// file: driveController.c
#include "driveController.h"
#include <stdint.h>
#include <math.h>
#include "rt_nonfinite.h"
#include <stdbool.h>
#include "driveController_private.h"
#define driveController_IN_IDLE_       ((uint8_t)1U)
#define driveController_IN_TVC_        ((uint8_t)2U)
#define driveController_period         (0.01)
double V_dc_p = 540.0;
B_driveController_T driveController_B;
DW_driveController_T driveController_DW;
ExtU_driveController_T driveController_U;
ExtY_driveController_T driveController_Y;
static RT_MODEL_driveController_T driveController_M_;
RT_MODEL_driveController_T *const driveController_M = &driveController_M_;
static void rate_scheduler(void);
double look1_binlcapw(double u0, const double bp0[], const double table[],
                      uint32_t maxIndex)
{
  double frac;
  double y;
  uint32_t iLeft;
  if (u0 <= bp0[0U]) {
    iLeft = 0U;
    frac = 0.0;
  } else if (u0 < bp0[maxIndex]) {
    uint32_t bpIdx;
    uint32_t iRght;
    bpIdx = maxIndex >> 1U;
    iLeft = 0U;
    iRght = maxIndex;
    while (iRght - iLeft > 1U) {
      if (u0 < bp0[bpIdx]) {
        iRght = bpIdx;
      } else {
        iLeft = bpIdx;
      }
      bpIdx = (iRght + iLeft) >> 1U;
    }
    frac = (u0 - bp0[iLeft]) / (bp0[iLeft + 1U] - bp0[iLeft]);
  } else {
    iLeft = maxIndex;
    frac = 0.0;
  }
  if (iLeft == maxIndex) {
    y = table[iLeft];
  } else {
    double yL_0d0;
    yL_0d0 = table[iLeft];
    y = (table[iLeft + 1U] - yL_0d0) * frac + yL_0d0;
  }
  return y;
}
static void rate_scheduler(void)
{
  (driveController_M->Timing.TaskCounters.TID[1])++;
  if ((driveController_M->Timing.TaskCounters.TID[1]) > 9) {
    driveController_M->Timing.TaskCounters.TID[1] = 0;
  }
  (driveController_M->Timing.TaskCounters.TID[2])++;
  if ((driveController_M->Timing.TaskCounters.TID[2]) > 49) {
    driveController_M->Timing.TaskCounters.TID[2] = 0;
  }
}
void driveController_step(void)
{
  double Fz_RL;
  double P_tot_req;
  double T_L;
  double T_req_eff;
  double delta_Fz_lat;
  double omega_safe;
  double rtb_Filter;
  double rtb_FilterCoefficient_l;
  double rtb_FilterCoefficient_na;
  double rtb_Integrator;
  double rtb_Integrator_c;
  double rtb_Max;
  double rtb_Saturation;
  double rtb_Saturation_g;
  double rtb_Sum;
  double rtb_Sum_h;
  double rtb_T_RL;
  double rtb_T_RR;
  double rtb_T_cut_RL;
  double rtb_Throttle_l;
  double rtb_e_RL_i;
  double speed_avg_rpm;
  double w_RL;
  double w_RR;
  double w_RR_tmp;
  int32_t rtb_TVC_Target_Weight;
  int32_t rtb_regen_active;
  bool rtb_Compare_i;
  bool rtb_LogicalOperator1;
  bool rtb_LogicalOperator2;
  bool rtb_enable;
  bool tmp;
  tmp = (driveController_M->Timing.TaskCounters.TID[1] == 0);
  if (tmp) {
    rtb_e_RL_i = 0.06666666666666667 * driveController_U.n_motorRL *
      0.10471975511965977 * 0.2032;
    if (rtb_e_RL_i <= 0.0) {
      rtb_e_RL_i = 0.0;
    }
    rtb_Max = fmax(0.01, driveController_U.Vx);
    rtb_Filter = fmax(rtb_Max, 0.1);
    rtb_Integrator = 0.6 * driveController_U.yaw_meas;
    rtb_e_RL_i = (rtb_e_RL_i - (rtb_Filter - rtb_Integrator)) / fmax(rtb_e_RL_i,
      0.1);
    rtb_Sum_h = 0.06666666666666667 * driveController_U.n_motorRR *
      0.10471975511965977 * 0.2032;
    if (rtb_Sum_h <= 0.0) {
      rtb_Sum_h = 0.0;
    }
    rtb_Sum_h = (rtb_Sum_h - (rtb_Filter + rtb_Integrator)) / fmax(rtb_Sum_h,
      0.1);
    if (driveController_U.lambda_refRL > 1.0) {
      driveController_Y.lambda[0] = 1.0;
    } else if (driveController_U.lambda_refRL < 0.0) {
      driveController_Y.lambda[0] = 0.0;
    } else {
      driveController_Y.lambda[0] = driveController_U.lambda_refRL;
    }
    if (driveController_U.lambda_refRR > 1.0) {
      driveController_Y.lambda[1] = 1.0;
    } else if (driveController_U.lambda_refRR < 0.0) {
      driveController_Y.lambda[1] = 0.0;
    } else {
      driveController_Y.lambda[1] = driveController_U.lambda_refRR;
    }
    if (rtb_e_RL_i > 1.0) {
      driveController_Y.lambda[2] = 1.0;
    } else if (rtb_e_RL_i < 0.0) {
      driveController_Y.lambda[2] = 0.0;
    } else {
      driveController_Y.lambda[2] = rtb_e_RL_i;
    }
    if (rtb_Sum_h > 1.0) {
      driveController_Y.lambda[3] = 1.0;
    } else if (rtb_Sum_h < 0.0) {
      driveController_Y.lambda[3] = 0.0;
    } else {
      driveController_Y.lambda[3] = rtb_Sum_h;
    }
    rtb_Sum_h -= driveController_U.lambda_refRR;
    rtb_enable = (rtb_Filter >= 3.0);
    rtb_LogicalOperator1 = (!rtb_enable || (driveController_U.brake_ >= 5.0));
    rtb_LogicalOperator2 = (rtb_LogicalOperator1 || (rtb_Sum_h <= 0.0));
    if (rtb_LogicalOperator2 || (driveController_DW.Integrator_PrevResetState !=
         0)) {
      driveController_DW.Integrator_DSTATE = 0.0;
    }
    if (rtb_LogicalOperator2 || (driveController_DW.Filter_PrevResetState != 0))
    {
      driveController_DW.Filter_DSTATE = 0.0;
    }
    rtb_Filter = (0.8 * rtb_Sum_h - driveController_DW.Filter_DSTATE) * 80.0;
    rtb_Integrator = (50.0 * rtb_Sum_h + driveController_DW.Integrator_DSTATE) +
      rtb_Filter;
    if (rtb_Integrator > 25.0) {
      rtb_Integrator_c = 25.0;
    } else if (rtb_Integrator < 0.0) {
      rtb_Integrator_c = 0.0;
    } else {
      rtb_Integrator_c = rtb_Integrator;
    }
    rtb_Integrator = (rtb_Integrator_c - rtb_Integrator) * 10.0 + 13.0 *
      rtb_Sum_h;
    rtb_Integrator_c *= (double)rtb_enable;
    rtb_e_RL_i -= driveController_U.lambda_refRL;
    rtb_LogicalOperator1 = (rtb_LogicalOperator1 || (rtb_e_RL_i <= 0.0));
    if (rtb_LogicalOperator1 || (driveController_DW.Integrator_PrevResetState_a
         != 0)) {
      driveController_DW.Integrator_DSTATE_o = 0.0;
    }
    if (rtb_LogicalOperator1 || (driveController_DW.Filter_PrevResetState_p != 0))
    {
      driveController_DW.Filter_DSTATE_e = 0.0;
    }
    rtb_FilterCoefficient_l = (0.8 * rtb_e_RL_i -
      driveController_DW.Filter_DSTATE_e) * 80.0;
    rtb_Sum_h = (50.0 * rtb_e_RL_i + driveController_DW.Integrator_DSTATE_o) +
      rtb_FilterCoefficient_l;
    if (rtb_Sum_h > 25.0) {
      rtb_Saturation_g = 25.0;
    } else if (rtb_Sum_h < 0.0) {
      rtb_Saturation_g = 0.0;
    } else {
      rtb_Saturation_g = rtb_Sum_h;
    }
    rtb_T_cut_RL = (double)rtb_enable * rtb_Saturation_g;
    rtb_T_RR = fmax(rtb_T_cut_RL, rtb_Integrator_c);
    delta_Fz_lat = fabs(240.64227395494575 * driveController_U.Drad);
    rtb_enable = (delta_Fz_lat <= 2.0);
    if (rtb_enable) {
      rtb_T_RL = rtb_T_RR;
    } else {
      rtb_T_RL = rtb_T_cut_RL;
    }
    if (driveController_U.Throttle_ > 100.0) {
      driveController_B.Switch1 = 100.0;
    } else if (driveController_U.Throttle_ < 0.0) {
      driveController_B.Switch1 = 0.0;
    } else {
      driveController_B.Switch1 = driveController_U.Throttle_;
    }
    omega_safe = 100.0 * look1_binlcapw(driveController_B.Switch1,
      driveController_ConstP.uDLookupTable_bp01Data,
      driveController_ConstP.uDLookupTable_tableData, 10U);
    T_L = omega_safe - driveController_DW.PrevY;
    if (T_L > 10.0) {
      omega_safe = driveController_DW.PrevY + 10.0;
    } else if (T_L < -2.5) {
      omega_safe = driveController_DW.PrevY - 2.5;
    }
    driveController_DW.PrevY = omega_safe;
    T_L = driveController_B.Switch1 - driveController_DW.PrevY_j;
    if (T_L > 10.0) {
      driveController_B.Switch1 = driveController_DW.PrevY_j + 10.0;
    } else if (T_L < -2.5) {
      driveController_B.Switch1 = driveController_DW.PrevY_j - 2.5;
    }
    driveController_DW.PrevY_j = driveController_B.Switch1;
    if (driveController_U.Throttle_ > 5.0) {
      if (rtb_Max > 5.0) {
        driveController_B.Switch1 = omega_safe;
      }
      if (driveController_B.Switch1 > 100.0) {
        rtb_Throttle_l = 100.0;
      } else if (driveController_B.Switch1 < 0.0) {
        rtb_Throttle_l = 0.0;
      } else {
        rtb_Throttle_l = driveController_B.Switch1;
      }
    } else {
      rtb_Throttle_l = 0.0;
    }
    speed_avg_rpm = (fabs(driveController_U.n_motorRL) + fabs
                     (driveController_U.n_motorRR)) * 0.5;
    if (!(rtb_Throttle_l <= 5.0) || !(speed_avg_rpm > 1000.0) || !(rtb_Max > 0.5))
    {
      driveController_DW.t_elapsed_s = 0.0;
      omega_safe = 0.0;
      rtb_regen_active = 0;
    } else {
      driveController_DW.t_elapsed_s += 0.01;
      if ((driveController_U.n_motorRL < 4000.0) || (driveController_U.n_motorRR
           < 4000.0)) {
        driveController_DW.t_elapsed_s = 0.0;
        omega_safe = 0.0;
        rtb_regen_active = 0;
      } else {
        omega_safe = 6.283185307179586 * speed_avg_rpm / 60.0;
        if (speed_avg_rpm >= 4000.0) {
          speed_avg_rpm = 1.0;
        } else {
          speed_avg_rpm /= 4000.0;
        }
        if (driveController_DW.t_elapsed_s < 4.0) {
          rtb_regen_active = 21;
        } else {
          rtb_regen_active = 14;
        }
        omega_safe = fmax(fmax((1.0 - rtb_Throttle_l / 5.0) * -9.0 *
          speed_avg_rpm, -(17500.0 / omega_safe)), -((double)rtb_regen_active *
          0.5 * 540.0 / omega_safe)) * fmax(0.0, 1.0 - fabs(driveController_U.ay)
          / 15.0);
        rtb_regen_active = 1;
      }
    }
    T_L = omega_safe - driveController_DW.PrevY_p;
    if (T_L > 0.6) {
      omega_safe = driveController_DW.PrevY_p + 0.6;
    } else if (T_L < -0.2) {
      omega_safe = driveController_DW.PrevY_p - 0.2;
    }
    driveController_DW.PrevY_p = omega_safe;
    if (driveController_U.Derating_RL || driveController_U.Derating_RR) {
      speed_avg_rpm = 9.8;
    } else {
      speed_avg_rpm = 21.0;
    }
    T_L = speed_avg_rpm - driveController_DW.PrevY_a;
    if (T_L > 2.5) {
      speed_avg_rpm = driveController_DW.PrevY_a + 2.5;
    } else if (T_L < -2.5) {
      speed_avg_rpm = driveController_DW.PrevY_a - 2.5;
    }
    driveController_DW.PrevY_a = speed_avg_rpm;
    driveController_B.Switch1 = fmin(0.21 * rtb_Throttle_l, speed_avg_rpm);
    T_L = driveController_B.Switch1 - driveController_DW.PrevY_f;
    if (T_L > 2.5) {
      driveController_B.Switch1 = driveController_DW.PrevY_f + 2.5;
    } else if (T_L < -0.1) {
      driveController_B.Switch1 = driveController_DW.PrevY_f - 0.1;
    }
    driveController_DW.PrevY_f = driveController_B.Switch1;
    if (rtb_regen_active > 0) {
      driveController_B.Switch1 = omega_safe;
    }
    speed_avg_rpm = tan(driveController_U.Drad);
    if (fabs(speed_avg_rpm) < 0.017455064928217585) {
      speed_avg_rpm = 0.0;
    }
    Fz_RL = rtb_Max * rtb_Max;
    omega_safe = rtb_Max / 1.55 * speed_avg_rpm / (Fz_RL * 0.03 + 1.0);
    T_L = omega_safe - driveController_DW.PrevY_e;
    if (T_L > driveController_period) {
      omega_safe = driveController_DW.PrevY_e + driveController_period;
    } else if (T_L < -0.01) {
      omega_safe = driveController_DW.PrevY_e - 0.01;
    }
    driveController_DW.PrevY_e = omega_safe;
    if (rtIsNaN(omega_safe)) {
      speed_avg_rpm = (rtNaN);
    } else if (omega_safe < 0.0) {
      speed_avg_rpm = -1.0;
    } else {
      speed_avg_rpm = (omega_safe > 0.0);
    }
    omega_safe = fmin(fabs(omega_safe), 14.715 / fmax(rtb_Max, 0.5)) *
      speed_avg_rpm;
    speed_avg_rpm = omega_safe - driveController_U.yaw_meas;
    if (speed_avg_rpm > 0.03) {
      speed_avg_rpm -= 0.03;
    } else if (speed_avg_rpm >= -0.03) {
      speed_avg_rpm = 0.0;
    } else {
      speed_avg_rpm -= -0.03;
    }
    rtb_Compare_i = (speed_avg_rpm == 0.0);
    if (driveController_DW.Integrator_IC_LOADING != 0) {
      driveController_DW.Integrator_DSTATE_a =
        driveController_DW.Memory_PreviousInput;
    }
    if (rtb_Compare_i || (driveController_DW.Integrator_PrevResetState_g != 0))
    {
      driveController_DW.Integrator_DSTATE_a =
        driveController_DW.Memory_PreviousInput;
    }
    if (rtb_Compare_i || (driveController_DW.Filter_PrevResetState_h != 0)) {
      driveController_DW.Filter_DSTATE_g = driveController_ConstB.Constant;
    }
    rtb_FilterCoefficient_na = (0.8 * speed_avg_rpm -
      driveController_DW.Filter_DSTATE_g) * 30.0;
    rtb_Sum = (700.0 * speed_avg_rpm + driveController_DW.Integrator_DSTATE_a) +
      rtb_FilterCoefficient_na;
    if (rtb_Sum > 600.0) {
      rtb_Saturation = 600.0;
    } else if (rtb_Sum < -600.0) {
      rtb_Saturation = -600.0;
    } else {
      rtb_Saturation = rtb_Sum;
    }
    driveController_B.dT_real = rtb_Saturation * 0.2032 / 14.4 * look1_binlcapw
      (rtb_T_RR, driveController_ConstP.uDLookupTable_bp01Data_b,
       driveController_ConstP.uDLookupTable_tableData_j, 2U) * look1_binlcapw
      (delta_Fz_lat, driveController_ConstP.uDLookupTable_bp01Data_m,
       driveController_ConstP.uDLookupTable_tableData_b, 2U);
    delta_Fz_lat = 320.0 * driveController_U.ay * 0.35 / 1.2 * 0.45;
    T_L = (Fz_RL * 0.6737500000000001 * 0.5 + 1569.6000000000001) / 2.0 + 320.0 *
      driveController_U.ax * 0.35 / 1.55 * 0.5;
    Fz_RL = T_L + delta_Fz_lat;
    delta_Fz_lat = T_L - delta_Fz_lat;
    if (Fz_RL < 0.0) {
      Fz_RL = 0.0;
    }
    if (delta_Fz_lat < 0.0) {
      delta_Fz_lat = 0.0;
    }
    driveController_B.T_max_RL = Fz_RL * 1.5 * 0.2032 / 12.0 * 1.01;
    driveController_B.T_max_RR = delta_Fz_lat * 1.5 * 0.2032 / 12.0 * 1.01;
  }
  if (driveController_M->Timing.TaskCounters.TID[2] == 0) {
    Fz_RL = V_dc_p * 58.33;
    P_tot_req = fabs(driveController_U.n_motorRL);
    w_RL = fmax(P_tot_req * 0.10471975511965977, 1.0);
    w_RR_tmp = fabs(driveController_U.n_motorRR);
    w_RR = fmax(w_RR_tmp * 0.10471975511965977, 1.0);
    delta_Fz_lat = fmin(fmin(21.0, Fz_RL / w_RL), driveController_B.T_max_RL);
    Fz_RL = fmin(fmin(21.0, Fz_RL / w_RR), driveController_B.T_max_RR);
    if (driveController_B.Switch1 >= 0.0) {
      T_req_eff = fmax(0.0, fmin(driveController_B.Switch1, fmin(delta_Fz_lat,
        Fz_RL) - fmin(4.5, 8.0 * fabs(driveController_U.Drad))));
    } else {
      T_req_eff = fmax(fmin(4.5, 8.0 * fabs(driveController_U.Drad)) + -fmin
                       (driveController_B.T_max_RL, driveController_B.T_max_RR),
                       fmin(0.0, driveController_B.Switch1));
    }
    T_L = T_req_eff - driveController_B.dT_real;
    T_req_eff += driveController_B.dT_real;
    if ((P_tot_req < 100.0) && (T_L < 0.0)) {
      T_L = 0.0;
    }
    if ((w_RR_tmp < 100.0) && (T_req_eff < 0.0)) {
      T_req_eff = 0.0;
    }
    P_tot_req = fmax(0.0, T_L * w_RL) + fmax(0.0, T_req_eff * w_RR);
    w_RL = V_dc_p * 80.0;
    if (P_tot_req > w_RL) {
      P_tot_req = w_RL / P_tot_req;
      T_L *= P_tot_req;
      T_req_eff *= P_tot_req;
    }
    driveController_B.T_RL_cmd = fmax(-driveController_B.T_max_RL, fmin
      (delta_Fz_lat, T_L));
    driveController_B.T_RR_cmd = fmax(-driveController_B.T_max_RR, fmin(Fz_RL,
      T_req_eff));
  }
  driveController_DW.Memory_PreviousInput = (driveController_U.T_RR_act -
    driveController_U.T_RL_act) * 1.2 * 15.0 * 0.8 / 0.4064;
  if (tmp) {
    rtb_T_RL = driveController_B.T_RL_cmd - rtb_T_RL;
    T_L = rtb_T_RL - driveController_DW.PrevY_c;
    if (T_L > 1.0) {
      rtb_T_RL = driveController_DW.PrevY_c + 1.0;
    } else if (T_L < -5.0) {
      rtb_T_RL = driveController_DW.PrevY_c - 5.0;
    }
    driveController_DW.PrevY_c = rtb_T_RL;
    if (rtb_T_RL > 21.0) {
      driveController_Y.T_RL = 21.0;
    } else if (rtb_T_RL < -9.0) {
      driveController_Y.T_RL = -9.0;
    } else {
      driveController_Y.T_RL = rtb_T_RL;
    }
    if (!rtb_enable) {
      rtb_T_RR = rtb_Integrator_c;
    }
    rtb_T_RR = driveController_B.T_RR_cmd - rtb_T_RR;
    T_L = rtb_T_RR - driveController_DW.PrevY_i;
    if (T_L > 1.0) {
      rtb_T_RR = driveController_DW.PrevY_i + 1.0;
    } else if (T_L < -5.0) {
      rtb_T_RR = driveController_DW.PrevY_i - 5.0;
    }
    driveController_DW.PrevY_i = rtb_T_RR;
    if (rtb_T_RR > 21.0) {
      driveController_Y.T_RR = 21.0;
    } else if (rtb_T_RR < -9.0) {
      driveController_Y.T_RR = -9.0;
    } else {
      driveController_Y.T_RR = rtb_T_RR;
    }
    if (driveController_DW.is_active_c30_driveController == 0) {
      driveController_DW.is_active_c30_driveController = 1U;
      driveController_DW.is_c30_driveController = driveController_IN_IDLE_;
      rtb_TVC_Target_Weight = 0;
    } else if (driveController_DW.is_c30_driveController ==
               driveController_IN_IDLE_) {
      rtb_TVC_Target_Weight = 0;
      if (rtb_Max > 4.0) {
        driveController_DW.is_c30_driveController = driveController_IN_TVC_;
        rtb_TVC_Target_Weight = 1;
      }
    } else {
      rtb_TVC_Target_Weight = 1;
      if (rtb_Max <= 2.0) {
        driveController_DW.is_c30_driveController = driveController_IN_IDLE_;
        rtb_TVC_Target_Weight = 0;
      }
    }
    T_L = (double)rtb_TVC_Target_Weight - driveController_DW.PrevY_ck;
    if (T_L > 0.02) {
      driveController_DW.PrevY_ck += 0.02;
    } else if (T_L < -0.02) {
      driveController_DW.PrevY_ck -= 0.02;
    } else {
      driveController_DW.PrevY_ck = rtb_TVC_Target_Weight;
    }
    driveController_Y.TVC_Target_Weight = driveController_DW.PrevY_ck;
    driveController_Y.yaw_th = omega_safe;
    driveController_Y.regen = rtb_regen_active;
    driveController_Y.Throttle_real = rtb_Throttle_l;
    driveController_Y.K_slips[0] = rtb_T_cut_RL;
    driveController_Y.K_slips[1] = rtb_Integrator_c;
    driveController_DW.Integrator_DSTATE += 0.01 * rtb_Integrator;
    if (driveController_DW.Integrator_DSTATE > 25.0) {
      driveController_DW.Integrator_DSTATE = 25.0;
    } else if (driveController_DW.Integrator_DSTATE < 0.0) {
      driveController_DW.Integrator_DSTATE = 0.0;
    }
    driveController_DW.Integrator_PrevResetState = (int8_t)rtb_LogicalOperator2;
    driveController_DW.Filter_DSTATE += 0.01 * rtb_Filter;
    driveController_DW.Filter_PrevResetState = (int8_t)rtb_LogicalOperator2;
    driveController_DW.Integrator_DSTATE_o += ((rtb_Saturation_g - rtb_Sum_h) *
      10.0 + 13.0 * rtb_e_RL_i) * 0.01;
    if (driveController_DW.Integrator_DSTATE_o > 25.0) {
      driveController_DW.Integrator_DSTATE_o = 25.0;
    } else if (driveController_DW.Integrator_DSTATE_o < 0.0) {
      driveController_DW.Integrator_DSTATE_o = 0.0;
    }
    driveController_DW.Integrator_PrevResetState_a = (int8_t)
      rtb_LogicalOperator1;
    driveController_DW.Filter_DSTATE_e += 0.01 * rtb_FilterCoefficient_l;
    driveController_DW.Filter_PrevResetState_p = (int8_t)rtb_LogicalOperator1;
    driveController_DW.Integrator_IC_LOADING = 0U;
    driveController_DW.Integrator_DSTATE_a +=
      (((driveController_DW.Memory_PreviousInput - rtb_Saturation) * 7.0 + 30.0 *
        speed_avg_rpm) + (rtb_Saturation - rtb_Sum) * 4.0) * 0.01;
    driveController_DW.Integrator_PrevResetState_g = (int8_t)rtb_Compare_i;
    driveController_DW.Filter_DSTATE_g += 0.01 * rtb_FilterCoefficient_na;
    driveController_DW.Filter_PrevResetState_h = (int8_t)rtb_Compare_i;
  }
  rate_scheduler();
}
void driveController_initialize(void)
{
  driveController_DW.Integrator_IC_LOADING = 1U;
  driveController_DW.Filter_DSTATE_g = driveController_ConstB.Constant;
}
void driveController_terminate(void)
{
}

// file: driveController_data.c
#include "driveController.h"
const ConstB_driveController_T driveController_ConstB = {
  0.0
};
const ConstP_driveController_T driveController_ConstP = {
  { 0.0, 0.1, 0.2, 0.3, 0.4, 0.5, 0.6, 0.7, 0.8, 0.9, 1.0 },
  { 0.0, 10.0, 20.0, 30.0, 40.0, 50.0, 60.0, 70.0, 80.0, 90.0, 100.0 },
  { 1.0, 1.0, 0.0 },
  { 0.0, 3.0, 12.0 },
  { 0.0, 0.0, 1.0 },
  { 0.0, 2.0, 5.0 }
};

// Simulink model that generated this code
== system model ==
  Throttle_ : Inport
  Vx : Inport
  ax : Inport
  ay : Inport
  Inport#1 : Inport
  Inport#2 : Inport
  brake_ : Inport
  T_RL_act : Inport
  T_RR_act : Inport
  Derating_RL : Inport
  Derating_RR : Inport
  n_motorRL : Inport
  n_motorRR : Inport
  lambda_refRL : Inport
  lambda_refRR : Inport
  T_RL : Outport  <- 1: Saturate#1
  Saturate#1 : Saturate  UpperLimit=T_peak  LowerLimit=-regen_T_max  <- 1: RateLimiter#1
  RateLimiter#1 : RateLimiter  RisingSlewLimit=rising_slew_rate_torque  FallingSlewLimit=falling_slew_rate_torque  <- 1: Sum#1
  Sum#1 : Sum  Inputs=+-  <- 1: MATLABFunction#1, 2: Switch#1
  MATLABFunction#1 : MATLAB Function  <- 1: Switch1, 2: Product#1, 3: n_motorRL, 4: n_motorRR, 5: Inport#2, 6: MATLABFunction#2, 7: MATLABFunction#2/2
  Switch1 : Switch  Criteria=u2 > Threshold  <- 1: RateLimiter#2, 2: MATLABFunction#3/2, 3: RateLimiter#3
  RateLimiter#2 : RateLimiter  RisingSlewLimit=60  FallingSlewLimit=-20  <- 1: MATLABFunction#3
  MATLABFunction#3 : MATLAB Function  <- 1: Switch#2, 2: n_motorRL, 3: n_motorRR, 4: Max, 5: ay
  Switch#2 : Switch  Criteria=u2 > Threshold  Threshold=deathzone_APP  <- 1: Saturation, 2: Throttle_, 3: Constant
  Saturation : Saturate  UpperLimit=100  LowerLimit=0  <- 1: Switch#3
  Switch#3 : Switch  Criteria=u2 > Threshold  Threshold=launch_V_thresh  <- 1: RateLimiter#4, 2: Max, 3: RateLimiter#5
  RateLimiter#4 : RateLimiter  RisingSlewLimit=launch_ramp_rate  FallingSlewLimit=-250  <- 1: Gain#1
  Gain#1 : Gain  Gain=100  <- 1: Lookup_nD#1
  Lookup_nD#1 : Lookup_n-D  BreakpointsForDimension1=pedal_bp  Table=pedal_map  <- 1: Saturate#2
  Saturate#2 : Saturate  UpperLimit=100  LowerLimit=0  <- 1: Throttle_
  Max : MinMax  Function=max  Inputs=2  <- 1: Constant#1, 2: Vx
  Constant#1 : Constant  Value=0.01
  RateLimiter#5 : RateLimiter  RisingSlewLimit=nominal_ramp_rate  FallingSlewLimit=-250  <- 1: Saturate#2
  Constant : Constant  Value=0
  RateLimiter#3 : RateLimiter  RisingSlewLimit=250  FallingSlewLimit=-10  <- 1: MinMax#1
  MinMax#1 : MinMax  Inputs=2  <- 1: Gain#2, 2: RateLimiter#6
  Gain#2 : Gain  Gain=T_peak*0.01  <- 1: Switch#2
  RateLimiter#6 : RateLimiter  RisingSlewLimit=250  FallingSlewLimit=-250  <- 1: Switch#4
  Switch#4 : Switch  Criteria=u2 > Threshold  Threshold=0.5  <- 1: Constant#2, 2: Logic#1, 3: Constant#3
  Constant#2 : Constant  Value=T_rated
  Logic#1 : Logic  Operator=OR  <- 1: Derating_RL, 2: Derating_RR
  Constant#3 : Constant  Value=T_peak
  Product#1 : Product  Inputs=3  <- 1: MATLABFunction#4, 2: Lookup_nD#2, 3: Lookup_nD#3
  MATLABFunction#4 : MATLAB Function  <- 1: PIDController#1
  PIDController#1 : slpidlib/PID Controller  Controller=PID  Form=Parallel  TimeDomain=Discrete-time  IntegratorMethod=Forward Euler  P=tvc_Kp  I=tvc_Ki  D=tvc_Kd  N=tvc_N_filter  InitialConditionForIntegrator=0  ExternalReset=level  LimitOutput=on  UpperSaturationLimit=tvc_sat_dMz  LowerSaturationLimit=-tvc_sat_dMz  <- 1: DeadZone#1, 2: CompareToConstant#1, 3: Memory, 4: Constant#4, 5: MATLABFunction#5
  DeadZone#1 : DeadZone  LowerValue=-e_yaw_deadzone  UpperValue=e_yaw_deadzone  <- 1: Sum
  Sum : Sum  Inputs=+-  <- 1: MATLABFunction#6, 2: Inport#1
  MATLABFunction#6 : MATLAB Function  <- 1: RateLimiter#7, 2: Max
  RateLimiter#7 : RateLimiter  <- 1: MATLABFunction#7
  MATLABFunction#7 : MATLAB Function  <- 1: Max, 2: MATLABFunction#8
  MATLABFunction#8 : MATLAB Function  <- 1: Trigonometry#1
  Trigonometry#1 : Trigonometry  Operator=tan  <- 1: Inport#2
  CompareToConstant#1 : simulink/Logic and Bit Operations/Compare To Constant  relop===  const=0  <- 1: DeadZone#1
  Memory : Memory  <- 1: MATLABFunction#5
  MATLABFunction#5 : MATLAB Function  <- 1: Sum#2
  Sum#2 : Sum  Inputs=-+  <- 1: T_RL_act, 2: T_RR_act
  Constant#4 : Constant  Value=0
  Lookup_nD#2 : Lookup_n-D  BreakpointsForDimension1=[0,3,12]  Table=[1,1,0]  <- 1: MinMax#2
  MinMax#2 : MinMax  Function=max  Inputs=2  <- 1: MATLABFunction#9, 2: MATLABFunction#10
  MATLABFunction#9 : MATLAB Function  <- 1: RelationalOperator#1, 2: Saturate#3
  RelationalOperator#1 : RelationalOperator  <- 1: MinMax#3, 2: Constant#5
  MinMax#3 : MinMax  Function=max  Inputs=2  <- 1: Max, 2: Constant#6
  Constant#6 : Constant  Value=0.1
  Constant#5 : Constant  Value=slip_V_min
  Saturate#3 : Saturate  UpperLimit=inf  LowerLimit=-2  <- 1: PIDController#2
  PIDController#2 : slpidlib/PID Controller  Controller=PID  Form=Parallel  TimeDomain=Discrete-time  IntegratorMethod=Forward Euler  P=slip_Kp  I=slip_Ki  D=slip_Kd  N=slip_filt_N  InitialConditionForIntegrator=0  ExternalReset=level  LimitOutput=on  UpperSaturationLimit=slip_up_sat  LowerSaturationLimit=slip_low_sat  <- 1: Sum#3, 2: LogicalOperator1
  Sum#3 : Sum  Inputs=-+  <- 1: lambda_refRL, 2: Product#2
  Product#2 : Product  Inputs=*/  <- 1: Sum#4, 2: MinMax#4
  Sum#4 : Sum  Inputs=+-  <- 1: Saturate#4, 2: Sum#5
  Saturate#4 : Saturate  UpperLimit=inf  LowerLimit=0  <- 1: Gain#3
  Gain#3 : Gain  Gain=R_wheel  <- 1: Gain#4
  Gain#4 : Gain  Gain=2*pi/60  <- 1: Gain#5
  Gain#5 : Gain  Gain=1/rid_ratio  <- 1: n_motorRL
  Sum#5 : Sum  Inputs=+-  <- 1: MinMax#3, 2: Gain#6
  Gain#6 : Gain  Gain=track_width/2  <- 1: Inport#1
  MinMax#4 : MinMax  Function=max  Inputs=2  <- 1: Saturate#4, 2: Constant#7
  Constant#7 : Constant  Value=0.1
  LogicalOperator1 : Logic  Operator=OR  Inputs=3  <- 1: Logic#2, 2: CompareToConstant#2, 3: CompareToConstant#3
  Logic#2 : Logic  Operator=NOT  <- 1: RelationalOperator#1
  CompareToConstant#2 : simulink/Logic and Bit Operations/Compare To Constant  relop=>=  const=5  <- 1: brake_
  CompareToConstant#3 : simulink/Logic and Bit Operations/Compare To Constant  relop=<=  const=0  <- 1: Sum#3
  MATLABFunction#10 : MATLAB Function  <- 1: RelationalOperator#1, 2: Saturate#5
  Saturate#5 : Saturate  UpperLimit=inf  LowerLimit=-2  <- 1: PIDController#3
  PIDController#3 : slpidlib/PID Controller  Controller=PID  Form=Parallel  TimeDomain=Discrete-time  IntegratorMethod=Forward Euler  P=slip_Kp  I=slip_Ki  D=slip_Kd  N=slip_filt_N  InitialConditionForIntegrator=0  ExternalReset=level  LimitOutput=on  UpperSaturationLimit=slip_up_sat  LowerSaturationLimit=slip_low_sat  <- 1: Sum#6, 2: LogicalOperator2
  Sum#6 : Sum  Inputs=-+  <- 1: lambda_refRR, 2: Product#3
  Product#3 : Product  Inputs=*/  <- 1: Sum#7, 2: MinMax#5
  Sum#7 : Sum  Inputs=+-  <- 1: Saturate#6, 2: Sum#8
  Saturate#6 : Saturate  UpperLimit=inf  LowerLimit=0  <- 1: Gain#7
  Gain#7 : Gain  Gain=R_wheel  <- 1: Gain#8
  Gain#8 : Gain  Gain=2*pi/60  <- 1: Gain#9
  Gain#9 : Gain  Gain=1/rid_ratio  <- 1: n_motorRR
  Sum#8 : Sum  <- 1: MinMax#3, 2: Gain#6
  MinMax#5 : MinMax  Function=max  Inputs=2  <- 1: Saturate#6, 2: Constant#8
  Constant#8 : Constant  Value=0.1
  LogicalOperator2 : Logic  Operator=OR  Inputs=3  <- 1: Logic#2, 2: CompareToConstant#2, 3: CompareToConstant#4
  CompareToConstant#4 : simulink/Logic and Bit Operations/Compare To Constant  relop=<=  const=0  <- 1: Sum#6
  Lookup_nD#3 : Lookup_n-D  BreakpointsForDimension1=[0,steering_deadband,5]  Table=[0,0,1]  <- 1: Abs#1
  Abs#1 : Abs  <- 1: Gain#10
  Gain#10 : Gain  Gain=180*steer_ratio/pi  <- 1: Inport#2
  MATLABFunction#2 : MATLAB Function  <- 1: Max, 2: ax, 3: ay
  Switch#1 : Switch  Criteria=u2 > Threshold  <- 1: MinMax#2, 2: CompareToConstant#5, 3: MATLABFunction#9
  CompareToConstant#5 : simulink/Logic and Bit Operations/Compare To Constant  relop=<=  const=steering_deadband  <- 1: Abs#2
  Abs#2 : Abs  <- 1: Gain#11
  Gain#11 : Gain  Gain=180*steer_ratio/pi  <- 1: Inport#2
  T_RR : Outport  <- 1: Saturate#7
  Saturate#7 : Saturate  UpperLimit=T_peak  LowerLimit=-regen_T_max  <- 1: RateLimiter#8
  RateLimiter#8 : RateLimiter  RisingSlewLimit=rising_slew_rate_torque  FallingSlewLimit=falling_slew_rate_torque  <- 1: Sum#9
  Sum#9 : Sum  Inputs=+-  <- 1: MATLABFunction#1/2, 2: Switch#5
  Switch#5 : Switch  Criteria=u2 > Threshold  <- 1: MinMax#2, 2: CompareToConstant#5, 3: MATLABFunction#10
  yaw_th : Outport  <- 1: MATLABFunction#6
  TVC_Target_Weight : Outport  <- 1: RateLimiter#9
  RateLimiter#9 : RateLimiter  RisingSlewLimit=2  FallingSlewLimit=-2  <- 1: Stateflowchart#1
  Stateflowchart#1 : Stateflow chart  <- 1: Max, 2: Inport#2, 3: Switch#2, 4: Sum, 5: brake_
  K_slips : Outport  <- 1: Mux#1
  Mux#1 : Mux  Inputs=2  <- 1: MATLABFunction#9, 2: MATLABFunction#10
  regen : Outport  <- 1: MATLABFunction#3/2
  lambda : Outport  <- 1: Saturate#8
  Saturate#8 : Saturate  UpperLimit=1  LowerLimit=0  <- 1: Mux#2
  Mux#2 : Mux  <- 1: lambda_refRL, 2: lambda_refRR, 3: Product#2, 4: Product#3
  Throttle_real : Outport  <- 1: Switch#2
== matlab function MATLAB Function ==
function T_cut_RL = fcn(enable, Delta_T_raw)
    T_cut_RL = enable * Delta_T_raw;
end

== matlab function MATLAB Function1 ==
function T_cut_RR = fcn(enable, Delta_T_raw)
    T_cut_RR = enable * Delta_T_raw;
end

== matlab function MATLAB Function ==
function dT = fcn(dMz, R_wheel, track_width, rid_ratio, rid_eff)
    dT = dMz * R_wheel / (track_width * rid_ratio * rid_eff);
end

== matlab function MATLAB Function1 ==
function dMz_act = fcn(dT_act, track_width, R_wheel, rid_ratio, rid_eff)
    %Yaw moment (z) that the engines are currently delivering
    dMz_act = dT_act * track_width * rid_ratio * rid_eff / (2 * R_wheel);
end

== matlab function MATLABFunction#1 ==
function [T_RL_cmd, T_RR_cmd] = fcn(T_req, dT, n_motorRL, n_motorRR, D, ...
    V_dc_p, T_peak, T_headroom_max, T_headroom_k, T_grip_max_RL, T_grip_max_RR, rpm_safe_threshold, I_discharge_max)
    T_min = 0;
    
    % --- CALCOLO POTENZA MASSIMA (Inverter) ---
    P_max_inverter = V_dc_p * 58.33; 
    
    % --- CALCOLO LIMITI ELETTRICI (FIELD WEAKENING) ---
    w_RL = max(abs(n_motorRL) * (pi/30), 1.0); 
    w_RR = max(abs(n_motorRR) * (pi/30), 1.0);
    
    T_fw_L = P_max_inverter / w_RL;
    T_fw_R = P_max_inverter / w_RR;
    
    T_elec_max_RL = min(T_peak, T_fw_L);
    T_elec_max_RR = min(T_peak, T_fw_R);
    
    % --- LIMITI FISICI GLOBALI ---
    T_max_L = min(T_elec_max_RL, T_grip_max_RL);
    T_max_R = min(T_elec_max_RR, T_grip_max_RR);
    
    % ---  PROTEZIONE ASIMMETRIA E HEADROOM TVC ---
    T_lim_base = min(T_max_L, T_max_R);
    T_headroom = min(T_headroom_max, T_headroom_k * abs(D));
    
    T_lim_base_neg = -min(T_grip_max_RL, T_grip_max_RR); 
    
    if T_req >= 0
        T_req_eff = max(0, min(T_req, T_lim_base - T_headroom));
    else
        T_req_eff = max(T_lim_base_neg + T_headroom, min(0, T_req));
    end
    
    % ---  TEORICO TVC ---
    T_L = T_req_eff - dT;
    T_R = T_req_eff + dT;
    
    if (abs(n_motorRL) < rpm_safe_threshold) && (T_L < 0)
        T_L = 0;
    end
    if (abs(n_motorRR) < rpm_safe_threshold) && (T_R < 0)
        T_R = 0;
    end
    
    % --- LIMITAZIONE PROPORZIONALE POTENZA DC (DC Current Limit) ---
    P_req_L = max(0, T_L * w_RL);
    P_req_R = max(0, T_R * w_RR);
    P_tot_req = P_req_L + P_req_R;
    
    P_limit_dc = V_dc_p * I_discharge_max;
    
    if P_tot_req > P_limit_dc
        scale_factor = P_limit_dc / P_tot_req;
        T_L = T_L * scale_factor;
        T_R = T_R * scale_factor;
    end
    
    % --- SATURAZIONE FINALE ---
    T_RL_cmd = max(-T_grip_max_RL, min(T_max_L, T_L));
    T_RR_cmd = max(-T_grip_max_RR, min(T_max_R, T_R));
end

== matlab function MATLABFunction#7 ==
function yaw_th = fcn(V,tan_delta,wheelbase,Kus)
% L = 1.55; %passo veicolo [m]
% yaw_th = (V / L) * tand;
%
  
yaw_th = (V / wheelbase) * tan_delta / (1 + Kus * V^2);

end

== matlab function MATLABFunction#8 ==
function tand_safe = fcn(tand,angle_limit_d)
    soglia = tan(angle_limit_d*pi/180);  % 2° rad
    
    if abs(tand) < soglia
        tand_safe = 0;  % 
    else
        tand_safe = tand;  
    end
end

== matlab function MATLABFunction#6 ==
function yaw_sat = fcn(yaw_th, V,mu, g)
    V_calc = max(V, 0.5);
    
    yaw_max_abs = (mu * g) / V_calc;
    yaw_sat = sign(yaw_th) * min(abs(yaw_th), yaw_max_abs);
end

== matlab function MATLAB Function ==
function [T_regen, regen_active] = regen_fcn( ...
        throttle_pct, n_motorRL, n_motorRR, V, Ts, ...
        regen_T_max, regen_pedal_thr, regen_speed_min_rpm, regen_speed_crit_rpm, ...
        regen_I_peak_A, regen_I_cont_A, regen_I_peak_dur_s, ...
        regen_P_batt_max_W, V_dc, ay, ay_limit, I_charge_max)

    persistent t_elapsed_s;
    if isempty(t_elapsed_s)
        t_elapsed_s = 0.0;
    end
    speed_avg_rpm = (abs(n_motorRL) + abs(n_motorRR)) * 0.5;
    
    % ---- condizione di abilitazione regen 
    should_regen = (throttle_pct <= regen_pedal_thr) && ...
                   (speed_avg_rpm > regen_speed_crit_rpm) && ...
                   (V > 0.5);
    if ~should_regen
        t_elapsed_s = 0.0;
        T_regen = 0;
        regen_active = 0.0;
        return;
    end
    
    t_elapsed_s = t_elapsed_s + Ts;
    
    % ---- Stage 1: coppia pedal-dipendente [Nm, negativa] ----------------
    pedal_norm = throttle_pct / regen_pedal_thr;
    T_s1 = -regen_T_max * (1.0 - pedal_norm);
    
    if n_motorRL < regen_speed_min_rpm || n_motorRR < regen_speed_min_rpm
        t_elapsed_s = 0.0;
        T_regen = 0;
        regen_active = 0.0;
        return;
    end
    % ---- Stage 2: fade-out velocità -------------------------------------
    if speed_avg_rpm >= regen_speed_min_rpm
        k_vel = 1.0;
    else
        k_vel = speed_avg_rpm / regen_speed_min_rpm;
    end
    T_s2 = T_s1 * k_vel;
    
    % ---- Stage 3: limite potenza batteria (per motore = totale/2) -------
    omega_rad_s = (2.0 * pi * speed_avg_rpm) / 60.0;
    omega_safe  = max(omega_rad_s, 1.0);          
    T_P_lim     = (regen_P_batt_max_W * 0.5) / omega_safe;
    T_s3        = max(T_s2, -T_P_lim);            
    
    % --- NUOVO: INCROCIO LIMITI DI CORRENTE BMS ---
    if t_elapsed_s < regen_I_peak_dur_s
        I_lim_teorico = regen_I_peak_A;    
    else
        I_lim_teorico = regen_I_cont_A;   
    end
    
    % Sceglie il limite più severo tra la logica timer e il CAN del BMS
    I_lim_effettivo = min(I_lim_teorico, I_charge_max);
    I_lim_per_mot = I_lim_effettivo * 0.5;
    
    T_I_lim = (I_lim_per_mot * V_dc) / omega_safe;
    T_final = max(T_s3, -T_I_lim);
    
    % ---- Stage 4: limite regen x curva ----------------------------------
    k_derating_ay = max(0.0, 1.0 - (abs(ay) / ay_limit));
    T_final = T_final * k_derating_ay;
    
    % ---- output simmetrico sui due motori -------------------------------
    T_regen  = T_final;
    regen_active = 1; 
end

== matlab function MATLAB Function1 ==
function [T_max_RL, T_max_RR] = GripEstimator(v_x, a_x, a_y, mass, g, wheelbase, l_f, track_width_r,mu,h_o, R_wheel,Af, Cl, aero_bal_r, K_roll_rear, rho, rid_ratio,rid_eff, overslip_factor)
    % ---------------------------------------------------------
    % 1. CARICO BASE (Statico + Aerodinamico)
    % ---------------------------------------------------------
    Fz_stat_rear = mass * g * (l_f / wheelbase);
    
    Fz_aero_rear = 0.5 * rho * Af * Cl * (v_x^2) * aero_bal_r;
    
    Fz_base_wheel = (Fz_stat_rear + Fz_aero_rear) / 2;

   
    % 2. TRASFERIMENTI DI CARICO
    % Longitudinale: se a_x > 0 (accelerazione), il peso si sposta dietro (+)
    delta_Fz_long = 0.5 * (mass * a_x * h_o / wheelbase);
    
    % Laterale: dipende dall'accelerazione laterale a_y.
    % Convenzione: a_y < 0 per curva a destra-> peso si sposta a sinistra.
    delta_Fz_lat = (mass * a_y * h_o / track_width_r) * K_roll_rear;

    % 3. FORZE NORMALI FINALI SULLE RUOTE (Fz)
    Fz_RL = Fz_base_wheel + delta_Fz_long + delta_Fz_lat;
    Fz_RR = Fz_base_wheel + delta_Fz_long - delta_Fz_lat;

    % Prevenzione valori negativi (se la ruota interna si alza da terra, Fz = 0)
    if Fz_RL < 0
        Fz_RL = 0;
    end
    if Fz_RR < 0
        Fz_RR = 0;
    end
    

    
    % 4. CALCOLO COPPIA MASSIMA AI MOTORI
    % T = (F * R) / (tau * eff)

    % Parametri Pacejka (dal file .tir)
    Fz0 = 1112.0;
    PDX1 = 1.00347;
    PDX2 = -0.99198;

    % Calcolo mu dinamico per lato sinistro
    dfz_RL = (Fz_RL - Fz0) / Fz0;
    mu_RL = PDX1 + (PDX2 * dfz_RL);
    
    % Saturazione di sicurezza (evita mu negativi o assurdi)
    if mu_RL < 0.5; mu_RL = 0.5; end

    % Calcolo mu dinamico per lato destro
    dfz_RR = (Fz_RR - Fz0) / Fz0;
    mu_RR = PDX1 + (PDX2 * dfz_RR);
    if mu_RR < 0.5; mu_RR = 0.5; end
    
   

    % % Calcolo coppia massima ai motori usando il mu corretto
    % T_max_RL = (Fz_RL * mu_RL * R_wheel) / (rid_ratio * rid_eff);
    % T_max_RR = (Fz_RR * mu_RR * R_wheel) / (rid_ratio * rid_eff);

    % Calcolo coppia massima ai motori
     %T_max_RL = ((Fz_RL * mu_RL * R_wheel) / (rid_ratio * rid_eff)) * overslip_factor;
     %T_max_RR = ((Fz_RR * mu_RR * R_wheel) / (rid_ratio * rid_eff)) * overslip_factor;

    T_max_RL = (Fz_RL * mu * R_wheel) / (rid_ratio * rid_eff)* overslip_factor;
    T_max_RR = (Fz_RR * mu * R_wheel) / (rid_ratio * rid_eff)* overslip_factor;
end

== stateflow chart Stateflowchart#1 ==
  state IDLE_
    entry:
    TVC_Target_Weight = 0;
  note: %[brake > 0 || (Throttle < tvc_throttle_on && V <= tvc_V_off)]
  state TVC_
    entry: TVC_Target_Weight = 1;
  (default) -> IDLE_
  TVC_ -> IDLE_ : [V <= tvc_V_off]
  IDLE_ -> TVC_ : [V > tvc_V_on]
  data: TVC_Target_Weight output; V input; D input; Throttle input; YawError input; brake input; tvc_D_thresh parameter; tvc_yaw_thresh parameter; tvc_yaw_thresh_off parameter; tvc_throttle_on parameter; tvc_V_on parameter; tvc_V_off parameter; tvc_D_thresh_off parameter
